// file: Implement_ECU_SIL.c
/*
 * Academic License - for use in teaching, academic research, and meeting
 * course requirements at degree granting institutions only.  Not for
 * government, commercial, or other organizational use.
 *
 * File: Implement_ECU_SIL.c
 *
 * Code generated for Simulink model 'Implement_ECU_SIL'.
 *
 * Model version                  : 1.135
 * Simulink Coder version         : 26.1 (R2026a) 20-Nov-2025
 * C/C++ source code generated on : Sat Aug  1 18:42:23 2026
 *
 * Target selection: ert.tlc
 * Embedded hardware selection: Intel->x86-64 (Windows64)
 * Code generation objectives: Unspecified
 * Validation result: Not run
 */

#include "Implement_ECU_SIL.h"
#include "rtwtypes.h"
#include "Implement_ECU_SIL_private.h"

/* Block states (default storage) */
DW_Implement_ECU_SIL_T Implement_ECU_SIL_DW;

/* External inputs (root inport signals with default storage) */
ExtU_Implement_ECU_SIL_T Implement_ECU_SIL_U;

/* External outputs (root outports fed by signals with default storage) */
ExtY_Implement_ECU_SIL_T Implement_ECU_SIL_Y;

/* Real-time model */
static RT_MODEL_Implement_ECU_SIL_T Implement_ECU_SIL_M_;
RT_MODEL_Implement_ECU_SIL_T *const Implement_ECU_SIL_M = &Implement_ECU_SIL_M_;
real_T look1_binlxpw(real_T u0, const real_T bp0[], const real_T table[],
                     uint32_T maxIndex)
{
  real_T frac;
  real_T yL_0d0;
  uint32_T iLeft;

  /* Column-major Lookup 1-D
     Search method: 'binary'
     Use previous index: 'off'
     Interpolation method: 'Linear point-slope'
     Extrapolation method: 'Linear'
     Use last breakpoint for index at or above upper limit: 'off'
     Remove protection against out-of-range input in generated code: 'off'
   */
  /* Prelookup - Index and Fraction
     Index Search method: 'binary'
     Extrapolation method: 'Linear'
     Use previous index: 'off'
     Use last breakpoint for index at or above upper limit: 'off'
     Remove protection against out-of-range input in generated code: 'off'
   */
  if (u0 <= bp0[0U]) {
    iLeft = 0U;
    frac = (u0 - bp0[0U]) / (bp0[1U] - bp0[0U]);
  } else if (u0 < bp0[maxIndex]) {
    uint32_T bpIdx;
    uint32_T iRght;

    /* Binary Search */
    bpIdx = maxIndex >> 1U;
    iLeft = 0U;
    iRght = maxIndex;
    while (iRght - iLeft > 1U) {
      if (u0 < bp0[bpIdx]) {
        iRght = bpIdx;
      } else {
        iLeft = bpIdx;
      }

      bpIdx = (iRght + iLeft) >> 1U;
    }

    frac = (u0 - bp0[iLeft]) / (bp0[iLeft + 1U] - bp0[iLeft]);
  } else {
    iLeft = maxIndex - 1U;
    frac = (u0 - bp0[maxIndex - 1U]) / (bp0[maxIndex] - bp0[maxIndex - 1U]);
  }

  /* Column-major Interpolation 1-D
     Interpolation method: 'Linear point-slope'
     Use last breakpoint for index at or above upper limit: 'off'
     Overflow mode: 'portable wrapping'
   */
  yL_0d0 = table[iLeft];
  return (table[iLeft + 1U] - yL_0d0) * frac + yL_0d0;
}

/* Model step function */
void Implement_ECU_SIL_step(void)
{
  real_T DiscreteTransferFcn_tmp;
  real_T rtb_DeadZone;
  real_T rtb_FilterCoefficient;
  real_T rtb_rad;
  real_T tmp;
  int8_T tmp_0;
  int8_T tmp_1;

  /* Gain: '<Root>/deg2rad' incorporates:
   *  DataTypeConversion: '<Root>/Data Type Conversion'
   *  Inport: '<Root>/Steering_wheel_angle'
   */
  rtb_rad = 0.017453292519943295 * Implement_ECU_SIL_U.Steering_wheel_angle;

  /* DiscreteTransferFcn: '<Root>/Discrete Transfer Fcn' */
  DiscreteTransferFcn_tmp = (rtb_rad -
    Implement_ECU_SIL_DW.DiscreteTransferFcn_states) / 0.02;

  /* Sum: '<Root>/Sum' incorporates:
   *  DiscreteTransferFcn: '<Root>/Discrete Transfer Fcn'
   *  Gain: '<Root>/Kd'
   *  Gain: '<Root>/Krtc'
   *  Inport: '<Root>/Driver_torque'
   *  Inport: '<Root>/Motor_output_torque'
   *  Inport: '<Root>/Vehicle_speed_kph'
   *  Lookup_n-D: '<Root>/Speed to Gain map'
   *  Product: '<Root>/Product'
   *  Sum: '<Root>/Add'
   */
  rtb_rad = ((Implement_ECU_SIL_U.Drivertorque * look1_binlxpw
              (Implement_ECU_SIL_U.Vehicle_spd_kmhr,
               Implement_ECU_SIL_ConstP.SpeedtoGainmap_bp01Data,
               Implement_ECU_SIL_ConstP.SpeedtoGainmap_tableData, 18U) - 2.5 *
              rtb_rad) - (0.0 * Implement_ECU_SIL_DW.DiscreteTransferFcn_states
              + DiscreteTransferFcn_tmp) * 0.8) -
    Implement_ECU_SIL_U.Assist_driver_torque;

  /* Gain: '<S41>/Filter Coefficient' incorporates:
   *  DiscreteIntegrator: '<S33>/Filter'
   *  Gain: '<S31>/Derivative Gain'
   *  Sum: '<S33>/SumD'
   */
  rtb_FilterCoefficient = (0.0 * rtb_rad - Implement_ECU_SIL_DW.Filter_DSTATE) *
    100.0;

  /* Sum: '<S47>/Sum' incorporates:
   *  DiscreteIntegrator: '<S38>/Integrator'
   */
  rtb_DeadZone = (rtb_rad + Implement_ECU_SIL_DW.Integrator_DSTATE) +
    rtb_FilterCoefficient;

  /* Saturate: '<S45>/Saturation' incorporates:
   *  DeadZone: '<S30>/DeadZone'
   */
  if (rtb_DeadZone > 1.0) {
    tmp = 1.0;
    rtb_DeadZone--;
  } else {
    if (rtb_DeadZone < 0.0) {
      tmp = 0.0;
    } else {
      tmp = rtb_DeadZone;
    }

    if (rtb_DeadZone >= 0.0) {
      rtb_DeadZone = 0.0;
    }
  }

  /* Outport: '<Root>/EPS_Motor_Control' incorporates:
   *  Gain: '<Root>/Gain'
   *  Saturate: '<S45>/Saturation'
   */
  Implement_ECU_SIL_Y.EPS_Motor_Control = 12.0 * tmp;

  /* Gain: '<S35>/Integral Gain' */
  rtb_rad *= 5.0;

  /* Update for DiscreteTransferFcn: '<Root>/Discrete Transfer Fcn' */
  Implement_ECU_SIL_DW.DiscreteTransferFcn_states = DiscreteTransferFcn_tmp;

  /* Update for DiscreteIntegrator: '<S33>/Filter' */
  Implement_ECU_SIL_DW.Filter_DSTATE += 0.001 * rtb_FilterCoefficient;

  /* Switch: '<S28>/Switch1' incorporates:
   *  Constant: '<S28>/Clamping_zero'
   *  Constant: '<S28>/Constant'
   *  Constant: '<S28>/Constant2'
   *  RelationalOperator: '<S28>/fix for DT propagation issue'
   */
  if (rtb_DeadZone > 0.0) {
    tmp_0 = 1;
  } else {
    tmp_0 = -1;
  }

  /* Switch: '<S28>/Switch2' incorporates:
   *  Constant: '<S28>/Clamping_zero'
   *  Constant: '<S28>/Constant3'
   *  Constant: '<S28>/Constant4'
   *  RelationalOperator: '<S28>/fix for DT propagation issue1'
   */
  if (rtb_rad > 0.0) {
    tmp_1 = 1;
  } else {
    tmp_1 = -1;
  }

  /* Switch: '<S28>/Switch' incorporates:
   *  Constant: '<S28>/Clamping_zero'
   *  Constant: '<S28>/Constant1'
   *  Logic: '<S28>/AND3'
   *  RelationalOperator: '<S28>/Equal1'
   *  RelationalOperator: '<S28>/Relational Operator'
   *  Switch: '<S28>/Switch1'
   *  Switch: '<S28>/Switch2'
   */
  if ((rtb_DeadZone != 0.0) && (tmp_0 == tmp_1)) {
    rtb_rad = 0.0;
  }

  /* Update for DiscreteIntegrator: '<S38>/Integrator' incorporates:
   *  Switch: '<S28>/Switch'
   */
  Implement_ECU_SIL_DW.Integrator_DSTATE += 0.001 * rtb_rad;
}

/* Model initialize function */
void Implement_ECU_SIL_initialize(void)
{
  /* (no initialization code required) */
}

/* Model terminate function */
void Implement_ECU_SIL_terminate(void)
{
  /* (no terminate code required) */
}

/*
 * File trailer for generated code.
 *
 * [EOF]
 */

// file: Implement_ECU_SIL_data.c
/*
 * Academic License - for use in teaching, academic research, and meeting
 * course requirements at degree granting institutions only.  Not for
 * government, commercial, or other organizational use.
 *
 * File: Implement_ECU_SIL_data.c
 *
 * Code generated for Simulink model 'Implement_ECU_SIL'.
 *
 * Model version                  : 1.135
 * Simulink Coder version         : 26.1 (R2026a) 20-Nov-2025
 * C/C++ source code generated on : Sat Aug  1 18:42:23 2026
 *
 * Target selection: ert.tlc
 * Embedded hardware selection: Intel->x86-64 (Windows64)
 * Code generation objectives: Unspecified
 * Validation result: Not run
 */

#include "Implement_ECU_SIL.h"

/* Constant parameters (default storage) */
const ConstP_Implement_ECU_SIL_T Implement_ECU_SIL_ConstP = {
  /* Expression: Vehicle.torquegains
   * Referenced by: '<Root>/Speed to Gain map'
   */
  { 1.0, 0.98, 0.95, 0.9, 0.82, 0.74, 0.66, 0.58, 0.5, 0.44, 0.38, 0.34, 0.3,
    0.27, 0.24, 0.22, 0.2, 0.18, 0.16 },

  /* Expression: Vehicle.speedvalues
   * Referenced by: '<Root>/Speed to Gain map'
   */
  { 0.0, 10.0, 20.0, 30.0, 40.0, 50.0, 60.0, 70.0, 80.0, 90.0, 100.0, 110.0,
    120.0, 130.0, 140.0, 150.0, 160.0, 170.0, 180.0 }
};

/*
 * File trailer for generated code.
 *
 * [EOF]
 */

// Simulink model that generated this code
simulink model "Implement_ECU_SIL"  (R2026a)
settings: Solver=FixedStepDiscrete  StopTime=50  FixedStep=0.001  RelTol=1e-6
InitFcn:
  | run('Vehicle_parameters_values_V1_MIL.m')
undefined symbols (not defined in the file): Vehicle
libraries: slpidlib x1

== system Implement_ECU_SIL ==
  Driver_torque : Inport  OutDataTypeStr=double  PortDimensions=1
  Vehicle_speed_kph : Inport  Port=2  OutDataTypeStr=double  PortDimensions=1
  Steering_wheel_angle : Inport  Port=3  OutDataTypeStr=single  PortDimensions=1
  Motor_output_torque : Inport  Port=4  OutDataTypeStr=double  PortDimensions=1
  Add : Sum  Inputs=+--
  Data Type Conversion : DataTypeConversion  OutDataTypeStr=double  SaturateOnIntegerOverflow=off  RndMeth=Floor
  Discrete Transfer Fcn : DiscreteTransferFcn  Numerator=[1 0]  Denominator=[0.02 1]
  Gain : Gain  Gain=12
  Kd : Gain  Gain=0.8
  Krtc : Gain  Gain=2.5
  PID Controller1 : slpidlib/PID Controller  Controller=PID  Form=Parallel  TimeDomain=Discrete-time  UseExternalTs=off  SampleTime=-1  IntegratorMethod=Forward Euler  FilterMethod=Forward Euler  ControllerParametersSource=internal  P=1  I=1.5  UseKiTs=off  D=0  UseExternalDerivativeSource=off  N=100  UseFilter=on  TunerSelectOption=Transfer Function Based (PID Tuner App)  InitialConditionSource=internal  InitialConditionForIntegrator=0  InitialConditionForFilter=0  DifferentiatorICPrevScaledInput=0  ExternalReset=none  TrackingMode=off  Kt=1  LimitOutput=on  SatLimitsSource=internal  UpperSaturationLimit=1  LowerSaturationLimit=0  LinearizeAsGain=on  AntiWindupMode=clamping  Kb=1  LimitIntegrator=off  UpperIntegratorSaturationLimit=inf  LowerIntegratorSaturationLimit=-inf  POutMin=[]  POutMax=[]  IOutMin=[]  IOutMax=[]  DOutMin=[]  DOutMax=[]  NOutMin=[]  NOutMax=[]  SumOutMin=[]  SumOutMax=[]  SaturationOutMin=[]  SaturationOutMax=[]  PParamMin=[]  PParamMax=[]  IParamMin=[]  IParamMax=[]  DParamMin=[]  DParamMax=[]  NParamMin=[]  NParamMax=[]  KbParamMin=[]  KbParamMax=[]  KtParamMin=[]  KtParamMax=[]  KbOutMin=[]  KbOutMax=[]  KtOutMin=[]  KtOutMax=[]  IntegratorOutMin=[]  IntegratorOutMax=[]  FilterOutMin=[]  FilterOutMax=[]  SumI1OutMin=[]  SumI1OutMax=[]  SumI2OutMin=[]  SumI2OutMax=[]  SumI3OutMin=[]  SumI3OutMax=[]  SumI4OutMin=[]  SumI4OutMax=[]  SumDOutMin=[]  SumDOutMax=[]  DifferentiatorOutMin=[]  DifferentiatorOutMax=[]  FilterDiffOutCoefMin=[]  FilterDiffOutCoefMax=[]  ReciprocalOutMin=[]  ReciprocalOutMax=[]  SumDenOutMin=[]  SumDenOutMax=[]  SumNumOutMin=[]  SumNumOutMax=[]  DivideOutMin=[]  DivideOutMax=[]  UdiffTsProdOutMin=[]  UdiffTsProdOutMax=[]  NTsProdOutMin=[]  NTsProdOutMax=[]  UintegralTsProdOutMin=[]  UintegralTsProdOutMax=[]  UngainTsProdOutMin=[]  UngainTsProdOutMax=[]  ClampingZeroOutDataTypeStr=Inherit: Inherit via back propagation  ClampingZeroOutMin=[]  ClampingZeroOutMax=[]  FilterDenConstantOutDataTypeStr=Inherit: Inherit via back propagation  FilterDenConstantOutMin=[]  FilterDenConstantOutMax=[]  PCopyOutDataTypeStr=Inherit: Inherit via back propagation  PCopyOutMin=[]  PCopyOutMax=[]  NCopyOutDataTypeStr=Inherit: Inherit via back propagation  NCopyOutMin=[]  NCopyOutMax=[]  IntegratorContinuousStateAttributes=''  IntegratorStateMustResolveToSignalObject=off  IntegratorRTWStateStorageClass=Auto  FilterContinuousStateAttributes=''  FilterStateMustResolveToSignalObject=off  FilterRTWStateStorageClass=Auto  ParallelPVariant=InternalParameters  IdealPVariant=Disabled  IVariant=InternalParameters  DVariant=InternalParameters  IntegratorVariant=Discrete  SatVariant=Enabled  AWVariant=DiscClampingParallel  PCopyVariant=Disabled  TRVariant=Disabled  FdbkBlocksVariant=Forward  IdealPFdbkVariant=Disabled  SatFdbkVariant=Disabled  DerivativeFilterVariant=ForwardEulerFilter  NVariant=InternalParameters  NCopyVariant=Disabled  FilterICVariant=InternalICsFilter  IntegratorICVariant=InternalICs  ExternalResetVariant=Disabled  TRSumVariant=Passthrough  SumFdbkVariant=Disabled  SumVariant=Sum_PID  TsampFilterVariant=InternalTs  TsampNgainVariant=Passthrough  TsampIntegralVariant=Disabled_SignalSpec  ExternalSaturationOutDataTypeStr=Inherit: Same as second input  DerivativeSourceVariant=ErrorSignal  PreIntVariant=InternalPreInt
  Product : Product
  Rate Transition{,1..4} (5 alike) : RateTransition  OutPortSampleTimeOpt=Inherit
  Saturation : Saturate  UpperLimit=1  LowerLimit=0
  Scope{,1..3} (4 alike) : Scope
  Speed to Gain map : Lookup_n-D  NumberOfTableDimensions=1  BreakpointsForDimension1=Vehicle.speedvalues  Table=Vehicle.torquegains  InternalRulePriority=Speed  RndMeth=Simplest
  Sum : Sum  Inputs=|+-
  deg2rad : Gain  Gain=pi/180
  EPS_Motor_Control : Outport  OutDataTypeStr=double  PortDimensions=1
  wires:
  Speed to Gain map/1 -> Scope3/1, Product/2  "Gain"
  Product/1 -> Add/1, Scope/1  "proportional_torque"
  Driver_torque/1 -> Rate Transition/1  "Driver torque"
  Vehicle_speed_kph/1 -> Rate Transition1/1  "Vehicle_spd_kmhr"
  PID Controller1/1 -> Saturation/1
  Motor_output_torque/1 -> Rate Transition3/1  "Assist_driver_torque"
  Saturation/1 -> Gain/1
  Gain/1 -> Rate Transition4/1
  Krtc/1 -> Add/2
  Steering_wheel_angle/1 -> Rate Transition2/1  "Steering_wheel_angle"
  deg2rad/1 -> Discrete Transfer Fcn/1, Krtc/1  "rad"
  Discrete Transfer Fcn/1 -> Kd/1  "rad.dot"
  Add/1 -> Sum/1, Scope2/1  "desired torque"
  Data Type Conversion/1 -> deg2rad/1
  Rate Transition/1 -> Product/1, Scope1/1
  Rate Transition1/1 -> Speed to Gain map/1
  Rate Transition2/1 -> Data Type Conversion/1
  Rate Transition4/1 -> EPS_Motor_Control/1
  Rate Transition3/1 -> Sum/2
  Kd/1 -> Add/3
  Sum/1 -> PID Controller1/1
